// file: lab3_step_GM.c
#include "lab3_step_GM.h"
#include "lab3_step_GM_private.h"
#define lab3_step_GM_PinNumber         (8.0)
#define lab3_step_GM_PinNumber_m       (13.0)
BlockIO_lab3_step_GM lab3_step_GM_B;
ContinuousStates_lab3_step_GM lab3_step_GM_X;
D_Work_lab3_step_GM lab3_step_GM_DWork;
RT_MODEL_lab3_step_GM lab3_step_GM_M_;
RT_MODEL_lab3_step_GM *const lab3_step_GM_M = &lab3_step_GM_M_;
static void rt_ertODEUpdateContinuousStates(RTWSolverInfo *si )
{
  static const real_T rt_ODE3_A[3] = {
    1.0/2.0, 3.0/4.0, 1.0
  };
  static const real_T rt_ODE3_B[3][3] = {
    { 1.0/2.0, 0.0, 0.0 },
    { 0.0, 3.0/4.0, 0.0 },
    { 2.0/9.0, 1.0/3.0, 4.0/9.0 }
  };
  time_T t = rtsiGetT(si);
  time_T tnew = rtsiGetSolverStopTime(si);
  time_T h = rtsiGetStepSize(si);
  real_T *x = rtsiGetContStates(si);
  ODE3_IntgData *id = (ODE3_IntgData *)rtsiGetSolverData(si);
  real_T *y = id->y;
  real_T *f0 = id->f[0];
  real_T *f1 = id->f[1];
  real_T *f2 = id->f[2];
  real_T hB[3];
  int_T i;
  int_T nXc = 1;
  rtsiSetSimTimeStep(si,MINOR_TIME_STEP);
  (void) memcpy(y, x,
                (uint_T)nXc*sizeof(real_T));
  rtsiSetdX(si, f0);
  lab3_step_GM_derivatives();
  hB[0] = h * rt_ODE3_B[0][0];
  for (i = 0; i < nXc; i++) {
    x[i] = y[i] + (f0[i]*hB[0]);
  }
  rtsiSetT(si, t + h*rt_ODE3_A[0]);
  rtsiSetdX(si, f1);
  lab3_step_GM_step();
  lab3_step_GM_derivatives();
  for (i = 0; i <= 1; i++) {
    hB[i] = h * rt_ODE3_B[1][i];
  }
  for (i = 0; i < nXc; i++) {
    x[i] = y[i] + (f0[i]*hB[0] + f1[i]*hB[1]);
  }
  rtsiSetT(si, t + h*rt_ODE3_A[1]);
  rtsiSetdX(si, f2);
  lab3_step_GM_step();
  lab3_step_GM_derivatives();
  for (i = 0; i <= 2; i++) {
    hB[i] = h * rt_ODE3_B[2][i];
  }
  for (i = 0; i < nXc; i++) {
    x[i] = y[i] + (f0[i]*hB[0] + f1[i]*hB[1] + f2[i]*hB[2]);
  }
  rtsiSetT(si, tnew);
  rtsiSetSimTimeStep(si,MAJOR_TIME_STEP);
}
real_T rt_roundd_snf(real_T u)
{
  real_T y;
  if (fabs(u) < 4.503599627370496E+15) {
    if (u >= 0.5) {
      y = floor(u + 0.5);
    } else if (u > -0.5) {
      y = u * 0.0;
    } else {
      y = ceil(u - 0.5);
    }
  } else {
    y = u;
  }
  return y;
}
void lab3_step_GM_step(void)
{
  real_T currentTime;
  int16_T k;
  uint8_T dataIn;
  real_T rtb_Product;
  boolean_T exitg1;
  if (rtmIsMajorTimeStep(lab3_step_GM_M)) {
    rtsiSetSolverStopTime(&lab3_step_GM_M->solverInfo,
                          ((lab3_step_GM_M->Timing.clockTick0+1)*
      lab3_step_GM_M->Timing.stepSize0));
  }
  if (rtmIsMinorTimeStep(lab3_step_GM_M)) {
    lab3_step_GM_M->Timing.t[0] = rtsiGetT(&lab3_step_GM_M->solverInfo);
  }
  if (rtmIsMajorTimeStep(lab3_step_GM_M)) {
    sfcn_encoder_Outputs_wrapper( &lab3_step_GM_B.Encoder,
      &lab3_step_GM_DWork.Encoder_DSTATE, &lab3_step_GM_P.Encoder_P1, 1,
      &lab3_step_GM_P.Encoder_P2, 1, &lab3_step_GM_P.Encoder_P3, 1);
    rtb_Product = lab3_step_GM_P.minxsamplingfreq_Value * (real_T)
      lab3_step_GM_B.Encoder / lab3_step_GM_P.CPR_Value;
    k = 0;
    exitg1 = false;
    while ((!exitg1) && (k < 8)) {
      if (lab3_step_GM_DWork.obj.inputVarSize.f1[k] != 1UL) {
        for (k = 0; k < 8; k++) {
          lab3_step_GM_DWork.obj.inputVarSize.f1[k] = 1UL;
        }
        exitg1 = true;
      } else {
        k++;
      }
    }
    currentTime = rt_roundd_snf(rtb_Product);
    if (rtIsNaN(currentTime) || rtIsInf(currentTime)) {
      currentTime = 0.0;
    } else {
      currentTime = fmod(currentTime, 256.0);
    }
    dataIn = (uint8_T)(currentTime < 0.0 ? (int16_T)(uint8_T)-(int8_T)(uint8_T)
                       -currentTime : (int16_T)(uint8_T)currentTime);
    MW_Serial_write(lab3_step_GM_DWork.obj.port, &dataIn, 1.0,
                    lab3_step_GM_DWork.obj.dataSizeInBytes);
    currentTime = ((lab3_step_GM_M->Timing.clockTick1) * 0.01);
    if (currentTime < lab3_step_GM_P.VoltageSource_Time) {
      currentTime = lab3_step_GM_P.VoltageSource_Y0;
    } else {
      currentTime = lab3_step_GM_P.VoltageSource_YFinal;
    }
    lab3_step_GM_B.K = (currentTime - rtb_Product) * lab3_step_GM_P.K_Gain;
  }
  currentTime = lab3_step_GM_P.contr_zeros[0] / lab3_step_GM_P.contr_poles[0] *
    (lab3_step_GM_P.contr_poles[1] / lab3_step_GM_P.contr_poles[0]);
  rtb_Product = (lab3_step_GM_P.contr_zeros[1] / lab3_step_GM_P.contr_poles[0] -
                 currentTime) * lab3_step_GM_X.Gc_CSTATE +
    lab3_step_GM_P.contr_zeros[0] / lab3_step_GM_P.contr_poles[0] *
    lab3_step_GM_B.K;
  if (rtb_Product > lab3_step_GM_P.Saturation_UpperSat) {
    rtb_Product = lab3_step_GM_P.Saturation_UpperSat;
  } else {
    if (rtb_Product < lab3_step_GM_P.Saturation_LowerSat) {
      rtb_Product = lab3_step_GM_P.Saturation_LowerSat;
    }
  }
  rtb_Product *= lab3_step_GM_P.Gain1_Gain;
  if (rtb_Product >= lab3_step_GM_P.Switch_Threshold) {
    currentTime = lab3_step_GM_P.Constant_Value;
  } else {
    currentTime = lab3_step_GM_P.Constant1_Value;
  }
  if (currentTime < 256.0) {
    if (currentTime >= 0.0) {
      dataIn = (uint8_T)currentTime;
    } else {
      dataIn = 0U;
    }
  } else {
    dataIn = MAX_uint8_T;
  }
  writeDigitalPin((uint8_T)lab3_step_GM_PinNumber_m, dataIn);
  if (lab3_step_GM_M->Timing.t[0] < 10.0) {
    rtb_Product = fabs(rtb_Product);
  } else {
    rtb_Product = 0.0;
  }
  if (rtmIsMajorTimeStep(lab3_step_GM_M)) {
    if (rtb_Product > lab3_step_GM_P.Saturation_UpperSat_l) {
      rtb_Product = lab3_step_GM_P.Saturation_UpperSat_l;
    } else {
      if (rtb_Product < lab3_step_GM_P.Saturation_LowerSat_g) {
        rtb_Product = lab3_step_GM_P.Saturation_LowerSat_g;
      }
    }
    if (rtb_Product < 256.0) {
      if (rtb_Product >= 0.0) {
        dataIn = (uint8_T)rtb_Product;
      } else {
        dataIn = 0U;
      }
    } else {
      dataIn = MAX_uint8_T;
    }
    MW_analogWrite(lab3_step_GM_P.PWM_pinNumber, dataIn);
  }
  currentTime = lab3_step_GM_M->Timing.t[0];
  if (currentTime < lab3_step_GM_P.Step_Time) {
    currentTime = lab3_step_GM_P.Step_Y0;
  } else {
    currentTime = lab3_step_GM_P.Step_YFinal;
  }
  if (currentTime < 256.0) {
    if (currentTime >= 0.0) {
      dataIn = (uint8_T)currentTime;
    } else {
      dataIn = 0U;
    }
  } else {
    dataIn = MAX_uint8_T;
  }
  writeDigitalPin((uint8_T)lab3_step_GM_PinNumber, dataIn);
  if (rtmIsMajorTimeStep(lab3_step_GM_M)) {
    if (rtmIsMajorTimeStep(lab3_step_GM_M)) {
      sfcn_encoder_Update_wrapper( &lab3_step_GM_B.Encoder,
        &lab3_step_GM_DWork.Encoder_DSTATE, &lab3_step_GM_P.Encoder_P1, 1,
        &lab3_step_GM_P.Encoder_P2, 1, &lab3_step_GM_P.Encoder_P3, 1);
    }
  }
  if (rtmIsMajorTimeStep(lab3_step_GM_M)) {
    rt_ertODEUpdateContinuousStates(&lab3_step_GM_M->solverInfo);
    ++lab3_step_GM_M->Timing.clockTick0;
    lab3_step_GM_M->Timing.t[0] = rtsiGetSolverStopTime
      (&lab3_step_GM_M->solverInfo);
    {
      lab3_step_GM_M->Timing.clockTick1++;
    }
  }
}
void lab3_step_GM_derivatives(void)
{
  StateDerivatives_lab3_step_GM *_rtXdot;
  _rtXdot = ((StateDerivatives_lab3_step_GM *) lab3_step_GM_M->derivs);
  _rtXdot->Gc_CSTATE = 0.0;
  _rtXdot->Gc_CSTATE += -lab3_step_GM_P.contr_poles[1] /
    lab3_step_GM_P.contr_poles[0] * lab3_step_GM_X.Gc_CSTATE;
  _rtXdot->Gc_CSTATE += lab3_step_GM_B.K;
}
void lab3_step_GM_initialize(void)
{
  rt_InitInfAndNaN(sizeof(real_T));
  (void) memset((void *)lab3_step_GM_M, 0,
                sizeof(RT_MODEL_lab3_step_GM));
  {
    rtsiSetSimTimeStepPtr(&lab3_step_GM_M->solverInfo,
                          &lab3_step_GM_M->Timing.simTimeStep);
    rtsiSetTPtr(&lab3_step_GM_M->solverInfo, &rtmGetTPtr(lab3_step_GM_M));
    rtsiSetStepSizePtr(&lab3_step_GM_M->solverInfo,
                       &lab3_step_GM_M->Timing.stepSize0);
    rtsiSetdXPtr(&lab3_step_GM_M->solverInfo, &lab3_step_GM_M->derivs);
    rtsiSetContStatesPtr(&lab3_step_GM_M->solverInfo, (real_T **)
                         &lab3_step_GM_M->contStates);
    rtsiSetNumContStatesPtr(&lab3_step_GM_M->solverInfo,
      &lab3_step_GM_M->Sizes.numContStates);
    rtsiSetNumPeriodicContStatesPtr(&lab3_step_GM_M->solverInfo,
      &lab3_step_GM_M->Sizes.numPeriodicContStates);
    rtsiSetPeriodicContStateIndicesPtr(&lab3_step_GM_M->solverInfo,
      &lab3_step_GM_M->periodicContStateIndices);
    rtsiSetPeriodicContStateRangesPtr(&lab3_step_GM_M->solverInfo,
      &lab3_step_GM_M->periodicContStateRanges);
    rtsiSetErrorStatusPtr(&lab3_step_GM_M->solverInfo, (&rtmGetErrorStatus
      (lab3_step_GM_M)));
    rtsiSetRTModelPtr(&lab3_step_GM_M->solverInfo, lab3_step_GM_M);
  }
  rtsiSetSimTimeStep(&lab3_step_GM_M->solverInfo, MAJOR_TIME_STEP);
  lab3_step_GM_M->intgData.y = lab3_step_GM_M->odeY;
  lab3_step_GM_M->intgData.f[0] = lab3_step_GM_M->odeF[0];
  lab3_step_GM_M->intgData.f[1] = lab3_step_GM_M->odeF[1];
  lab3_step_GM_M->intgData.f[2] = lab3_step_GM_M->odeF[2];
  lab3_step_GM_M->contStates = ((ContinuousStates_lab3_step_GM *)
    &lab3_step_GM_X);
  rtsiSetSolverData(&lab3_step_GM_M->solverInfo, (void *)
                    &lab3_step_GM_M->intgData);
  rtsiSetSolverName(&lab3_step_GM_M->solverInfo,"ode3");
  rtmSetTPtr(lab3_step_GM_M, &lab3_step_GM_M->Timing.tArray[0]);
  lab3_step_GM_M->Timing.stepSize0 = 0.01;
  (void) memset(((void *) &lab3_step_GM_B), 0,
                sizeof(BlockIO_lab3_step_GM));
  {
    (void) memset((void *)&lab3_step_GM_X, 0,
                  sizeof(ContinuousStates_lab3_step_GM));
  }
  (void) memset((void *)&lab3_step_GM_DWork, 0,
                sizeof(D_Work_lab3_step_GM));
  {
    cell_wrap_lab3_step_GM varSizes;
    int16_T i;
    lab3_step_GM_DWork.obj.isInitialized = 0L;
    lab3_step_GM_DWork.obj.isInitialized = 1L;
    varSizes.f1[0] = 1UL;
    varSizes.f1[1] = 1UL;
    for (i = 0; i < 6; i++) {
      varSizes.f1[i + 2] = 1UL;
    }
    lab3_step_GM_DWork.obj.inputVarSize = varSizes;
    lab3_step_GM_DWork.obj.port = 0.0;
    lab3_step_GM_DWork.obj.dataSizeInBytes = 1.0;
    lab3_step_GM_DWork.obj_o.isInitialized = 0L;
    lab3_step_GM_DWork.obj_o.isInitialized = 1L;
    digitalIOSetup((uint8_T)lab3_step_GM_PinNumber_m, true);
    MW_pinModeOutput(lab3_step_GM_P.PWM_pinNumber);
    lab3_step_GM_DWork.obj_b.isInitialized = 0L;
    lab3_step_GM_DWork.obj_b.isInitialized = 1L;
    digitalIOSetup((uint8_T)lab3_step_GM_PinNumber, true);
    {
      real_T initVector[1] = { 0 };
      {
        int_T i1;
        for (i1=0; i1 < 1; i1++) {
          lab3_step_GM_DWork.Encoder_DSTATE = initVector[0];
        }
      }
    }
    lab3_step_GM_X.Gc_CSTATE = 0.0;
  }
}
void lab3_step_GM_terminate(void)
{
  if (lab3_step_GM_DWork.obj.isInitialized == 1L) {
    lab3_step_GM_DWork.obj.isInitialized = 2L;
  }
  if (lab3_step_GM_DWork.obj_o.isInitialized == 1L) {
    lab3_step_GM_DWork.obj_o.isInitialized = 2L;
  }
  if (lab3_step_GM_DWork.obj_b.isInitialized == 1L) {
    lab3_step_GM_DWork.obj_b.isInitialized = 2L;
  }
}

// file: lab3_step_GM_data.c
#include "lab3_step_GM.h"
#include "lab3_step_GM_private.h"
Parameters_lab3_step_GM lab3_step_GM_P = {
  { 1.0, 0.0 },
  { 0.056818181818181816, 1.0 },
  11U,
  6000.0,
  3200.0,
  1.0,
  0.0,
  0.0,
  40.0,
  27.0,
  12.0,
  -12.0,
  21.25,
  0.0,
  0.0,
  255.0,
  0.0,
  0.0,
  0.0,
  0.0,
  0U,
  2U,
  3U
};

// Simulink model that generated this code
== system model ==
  SerialTransmit#1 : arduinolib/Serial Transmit  <- 1: DataTypeConversion#1
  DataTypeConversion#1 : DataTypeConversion  <- 1: Product
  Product : Product  Inputs=**/  <- 1: minxsamplingfreq, 2: DataTypeConversion#2, 3: CPR
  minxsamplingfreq : Constant  Value=6000
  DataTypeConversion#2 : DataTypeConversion  <- 1: Encoder
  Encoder : S-Function  FunctionName=sfcn_encoder
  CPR : Constant  Value=3200
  DigitalOutput#1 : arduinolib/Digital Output  pinNumber=13  <- 1: hardlim#1
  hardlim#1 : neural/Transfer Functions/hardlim  <- 1: Gain1
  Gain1 : Gain  Gain=255/12  <- 1: Saturation
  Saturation : Saturate  UpperLimit=12  LowerLimit=-12  <- 1: Gc
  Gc : TransferFcn  Numerator=contr_zeros  Denominator=contr_poles  <- 1: Gain#1
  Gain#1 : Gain  Gain=27  <- 1: Sum#1
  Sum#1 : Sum  Inputs=+-  <- 1: VoltageSource, 2: Product
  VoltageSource : Step  Time=0  After=40
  PWM : arduinolib/PWM  pinNumber=11  <- 1: Saturate#1
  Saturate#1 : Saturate  UpperLimit=255  LowerLimit=0  <- 1: MATLABFunction#1
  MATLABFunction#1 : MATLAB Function  <- 1: Abs#1, 2: Clock#1
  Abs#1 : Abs  <- 1: Gain1
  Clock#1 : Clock
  DigitalOutput#2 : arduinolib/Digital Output  pinNumber=8  <- 1: Step
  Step : Step  Time=0  After=0
== matlab function MATLABFunction#1 ==
function y = fcn(u,c)
%#codegen
if c<10
    y = u;
else
    y=0;
end
